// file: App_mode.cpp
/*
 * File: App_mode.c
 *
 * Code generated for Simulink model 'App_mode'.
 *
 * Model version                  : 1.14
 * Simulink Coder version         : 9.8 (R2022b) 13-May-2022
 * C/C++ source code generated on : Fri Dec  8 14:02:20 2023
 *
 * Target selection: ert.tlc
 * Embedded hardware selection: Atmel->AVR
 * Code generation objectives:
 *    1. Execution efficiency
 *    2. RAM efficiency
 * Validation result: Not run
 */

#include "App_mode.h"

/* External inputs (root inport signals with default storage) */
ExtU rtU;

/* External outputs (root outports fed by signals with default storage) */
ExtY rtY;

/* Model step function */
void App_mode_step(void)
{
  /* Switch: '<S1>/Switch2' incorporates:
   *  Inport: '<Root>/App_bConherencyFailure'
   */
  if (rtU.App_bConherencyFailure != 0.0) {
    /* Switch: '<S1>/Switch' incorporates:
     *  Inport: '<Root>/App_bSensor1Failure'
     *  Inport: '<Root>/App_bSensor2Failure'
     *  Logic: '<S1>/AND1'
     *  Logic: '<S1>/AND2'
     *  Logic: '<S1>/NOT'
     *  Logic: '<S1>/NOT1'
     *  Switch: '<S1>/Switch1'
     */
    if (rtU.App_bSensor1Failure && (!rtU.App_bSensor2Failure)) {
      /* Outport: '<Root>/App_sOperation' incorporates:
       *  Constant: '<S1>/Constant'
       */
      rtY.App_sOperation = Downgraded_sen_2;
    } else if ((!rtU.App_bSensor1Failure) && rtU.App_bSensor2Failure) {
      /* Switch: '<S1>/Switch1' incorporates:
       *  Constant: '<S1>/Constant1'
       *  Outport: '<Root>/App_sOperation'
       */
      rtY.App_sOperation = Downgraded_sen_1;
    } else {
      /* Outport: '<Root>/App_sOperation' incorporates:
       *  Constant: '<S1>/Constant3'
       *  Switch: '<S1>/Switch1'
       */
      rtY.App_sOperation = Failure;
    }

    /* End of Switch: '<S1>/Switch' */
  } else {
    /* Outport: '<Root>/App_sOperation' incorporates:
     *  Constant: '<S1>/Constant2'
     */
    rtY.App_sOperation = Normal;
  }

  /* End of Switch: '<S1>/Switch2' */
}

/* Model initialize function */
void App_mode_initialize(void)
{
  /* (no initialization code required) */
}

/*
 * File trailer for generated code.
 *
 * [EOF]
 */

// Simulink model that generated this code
simulink model "App_mode"  (R2022b)
settings: Solver=FixedStepDiscrete  StartTime=0.0  StopTime=10.0  FixedStep=0.01  RelTol=1e-3
InitFcn:
  | Init
undefined symbols (not defined in the file): App_modes

== system App_mode ==
  App_bSensor1Failure : Inport
  App_bSensor2Failure : Inport  Port=2
  App_bConherencyFailure : Inport  Port=3
  App_Operation : Subsystem
  App_sOperation : Outport
  wires:
  App_Operation/1(App_sOperation) -> App_sOperation/1  "App_sOperation"
  App_bSensor1Failure/1 -> App_Operation/1(App_bSensor1Failure)  "App_bSensor1Failure"
  App_bConherencyFailure/1 -> App_Operation/3(App_bConherencyFailure)  "App_bConherencyFailure"
  App_bSensor2Failure/1 -> App_Operation/2(App_bSensor2Failure)  "App_bSensor2Failure"

== system App_mode/App_Operation ==
  App_bSensor1Failure : Inport
  App_bSensor2Failure : Inport  Port=2
  App_bConherencyFailure : Inport  Port=3
  AND1 : Logic  AllPortsSameDT=off  OutDataTypeStr=boolean
  AND2 : Logic  AllPortsSameDT=off  OutDataTypeStr=boolean
  Constant : Constant  Value=App_modes.Downgraded_sen_2  OutDataTypeStr=Enum: App_modes
  Constant1 : Constant  Value=App_modes.Downgraded_sen_1  OutDataTypeStr=Enum: App_modes
  Constant2 : Constant  Value=App_modes.Normal  OutDataTypeStr=Enum: App_modes
  Constant3 : Constant  Value=App_modes.Failure  OutDataTypeStr=Enum: App_modes
  NOT : Logic  Operator=NOT  IconShape=distinctive  AllPortsSameDT=off  OutDataTypeStr=boolean
  NOT1 : Logic  Operator=NOT  IconShape=distinctive  AllPortsSameDT=off  OutDataTypeStr=boolean
  Switch : Switch  Criteria=u2 ~= 0  SaturateOnIntegerOverflow=off  InputSameDT=off
  Switch1 : Switch  Criteria=u2 ~= 0  SaturateOnIntegerOverflow=off  InputSameDT=off
  Switch2 : Switch  Criteria=u2 ~= 0  SaturateOnIntegerOverflow=off  InputSameDT=off
  App_sOperation : Outport  OutDataTypeStr=Enum: App_modes  LockScale=on
  wires:
  NOT/1 -> AND1/2
  NOT1/1 -> AND2/1
  App_bSensor1Failure/1 -> NOT1/1, AND1/1
  App_bSensor2Failure/1 -> NOT/1, AND2/2
  AND1/1 -> Switch/2  "Downgraded sen1"
  AND2/1 -> Switch1/2  "Downgraded sen2"
  Switch/1 -> Switch2/1
  Switch2/1 -> App_sOperation/1
  App_bConherencyFailure/1 -> Switch2/2
  Switch1/1 -> Switch/3
  Constant/1 -> Switch/1
  Constant2/1 -> Switch2/3
  Constant1/1 -> Switch1/1
  Constant3/1 -> Switch1/3
